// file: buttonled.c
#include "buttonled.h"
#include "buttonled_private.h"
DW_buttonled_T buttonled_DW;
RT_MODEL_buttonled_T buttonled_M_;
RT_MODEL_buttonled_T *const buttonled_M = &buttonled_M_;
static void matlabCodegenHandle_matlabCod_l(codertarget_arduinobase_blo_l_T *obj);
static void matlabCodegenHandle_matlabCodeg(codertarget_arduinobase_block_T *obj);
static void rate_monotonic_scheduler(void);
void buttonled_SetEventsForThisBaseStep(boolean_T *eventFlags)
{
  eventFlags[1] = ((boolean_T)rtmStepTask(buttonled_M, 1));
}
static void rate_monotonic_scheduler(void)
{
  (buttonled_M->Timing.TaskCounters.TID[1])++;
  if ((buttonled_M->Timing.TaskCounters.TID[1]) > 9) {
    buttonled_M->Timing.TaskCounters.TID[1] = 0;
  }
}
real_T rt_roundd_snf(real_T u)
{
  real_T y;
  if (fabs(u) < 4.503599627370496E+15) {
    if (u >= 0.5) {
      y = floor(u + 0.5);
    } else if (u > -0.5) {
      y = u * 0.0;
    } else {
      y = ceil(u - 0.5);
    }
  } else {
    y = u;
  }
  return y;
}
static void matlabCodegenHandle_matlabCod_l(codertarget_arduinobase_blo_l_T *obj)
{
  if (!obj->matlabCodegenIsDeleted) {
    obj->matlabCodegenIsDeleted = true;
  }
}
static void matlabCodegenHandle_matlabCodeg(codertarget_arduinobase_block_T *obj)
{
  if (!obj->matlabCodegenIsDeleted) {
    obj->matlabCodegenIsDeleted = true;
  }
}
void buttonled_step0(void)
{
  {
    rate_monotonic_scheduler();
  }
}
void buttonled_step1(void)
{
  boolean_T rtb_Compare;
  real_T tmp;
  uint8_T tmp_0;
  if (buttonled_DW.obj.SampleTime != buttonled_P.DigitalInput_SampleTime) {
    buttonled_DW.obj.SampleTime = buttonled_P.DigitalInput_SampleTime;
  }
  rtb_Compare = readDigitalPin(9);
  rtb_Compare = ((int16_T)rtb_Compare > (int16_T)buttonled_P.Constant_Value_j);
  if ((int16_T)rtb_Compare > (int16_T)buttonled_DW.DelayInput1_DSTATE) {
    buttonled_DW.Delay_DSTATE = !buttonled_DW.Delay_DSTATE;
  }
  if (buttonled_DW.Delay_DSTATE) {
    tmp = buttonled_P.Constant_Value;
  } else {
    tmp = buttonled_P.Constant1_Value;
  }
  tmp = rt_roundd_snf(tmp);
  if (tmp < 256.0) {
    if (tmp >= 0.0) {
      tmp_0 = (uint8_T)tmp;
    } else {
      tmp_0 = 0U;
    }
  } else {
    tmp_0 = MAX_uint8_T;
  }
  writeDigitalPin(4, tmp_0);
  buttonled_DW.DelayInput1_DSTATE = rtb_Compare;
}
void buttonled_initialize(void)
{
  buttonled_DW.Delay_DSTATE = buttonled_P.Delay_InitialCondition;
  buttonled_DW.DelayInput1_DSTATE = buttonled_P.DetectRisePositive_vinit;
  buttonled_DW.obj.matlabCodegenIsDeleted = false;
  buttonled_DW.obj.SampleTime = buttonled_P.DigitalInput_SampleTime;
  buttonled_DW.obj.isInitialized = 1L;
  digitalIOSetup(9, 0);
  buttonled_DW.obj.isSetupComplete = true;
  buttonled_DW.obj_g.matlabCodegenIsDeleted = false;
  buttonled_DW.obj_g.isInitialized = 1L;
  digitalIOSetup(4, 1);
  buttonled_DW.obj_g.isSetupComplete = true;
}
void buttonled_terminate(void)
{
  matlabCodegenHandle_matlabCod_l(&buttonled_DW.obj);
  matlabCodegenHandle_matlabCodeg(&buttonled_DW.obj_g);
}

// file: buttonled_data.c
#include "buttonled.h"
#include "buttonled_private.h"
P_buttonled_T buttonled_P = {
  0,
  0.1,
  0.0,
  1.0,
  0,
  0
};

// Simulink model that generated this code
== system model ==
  DigitalOutput#1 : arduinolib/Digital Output  pinNumber=4  <- 1: Merge#1
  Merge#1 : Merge  <- 1: Subsystem#1, 2: Subsystem#2
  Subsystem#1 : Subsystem  <- 1: Constant, Action: If#1
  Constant : Constant
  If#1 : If  <- 1: DataTypeConversion#1
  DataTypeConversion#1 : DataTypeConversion
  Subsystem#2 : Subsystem  <- 1: Constant1, Action: If#1/2
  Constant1 : Constant  Value=0
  DigitalInput : arduinolib/Digital Input  pinNumber=9
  DetectRisePositive : simulink/Logic and Bit Operations/Detect Rise Positive  <- 1: DigitalInput
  Constant#1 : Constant
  Switch#1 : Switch  Criteria=u2 > Threshold  <- 1: Constant#1, 2: DetectRisePositive, 3: Delay
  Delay : Delay  DelayLength=1  <- 1: Switch#1
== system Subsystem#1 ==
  Inport#1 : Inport
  ActionPort#1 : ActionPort
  Outport#1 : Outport  <- 1: Inport#1
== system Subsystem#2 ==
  Inport#2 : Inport
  ActionPort#2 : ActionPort
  Outport#2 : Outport  <- 1: Inport#2
